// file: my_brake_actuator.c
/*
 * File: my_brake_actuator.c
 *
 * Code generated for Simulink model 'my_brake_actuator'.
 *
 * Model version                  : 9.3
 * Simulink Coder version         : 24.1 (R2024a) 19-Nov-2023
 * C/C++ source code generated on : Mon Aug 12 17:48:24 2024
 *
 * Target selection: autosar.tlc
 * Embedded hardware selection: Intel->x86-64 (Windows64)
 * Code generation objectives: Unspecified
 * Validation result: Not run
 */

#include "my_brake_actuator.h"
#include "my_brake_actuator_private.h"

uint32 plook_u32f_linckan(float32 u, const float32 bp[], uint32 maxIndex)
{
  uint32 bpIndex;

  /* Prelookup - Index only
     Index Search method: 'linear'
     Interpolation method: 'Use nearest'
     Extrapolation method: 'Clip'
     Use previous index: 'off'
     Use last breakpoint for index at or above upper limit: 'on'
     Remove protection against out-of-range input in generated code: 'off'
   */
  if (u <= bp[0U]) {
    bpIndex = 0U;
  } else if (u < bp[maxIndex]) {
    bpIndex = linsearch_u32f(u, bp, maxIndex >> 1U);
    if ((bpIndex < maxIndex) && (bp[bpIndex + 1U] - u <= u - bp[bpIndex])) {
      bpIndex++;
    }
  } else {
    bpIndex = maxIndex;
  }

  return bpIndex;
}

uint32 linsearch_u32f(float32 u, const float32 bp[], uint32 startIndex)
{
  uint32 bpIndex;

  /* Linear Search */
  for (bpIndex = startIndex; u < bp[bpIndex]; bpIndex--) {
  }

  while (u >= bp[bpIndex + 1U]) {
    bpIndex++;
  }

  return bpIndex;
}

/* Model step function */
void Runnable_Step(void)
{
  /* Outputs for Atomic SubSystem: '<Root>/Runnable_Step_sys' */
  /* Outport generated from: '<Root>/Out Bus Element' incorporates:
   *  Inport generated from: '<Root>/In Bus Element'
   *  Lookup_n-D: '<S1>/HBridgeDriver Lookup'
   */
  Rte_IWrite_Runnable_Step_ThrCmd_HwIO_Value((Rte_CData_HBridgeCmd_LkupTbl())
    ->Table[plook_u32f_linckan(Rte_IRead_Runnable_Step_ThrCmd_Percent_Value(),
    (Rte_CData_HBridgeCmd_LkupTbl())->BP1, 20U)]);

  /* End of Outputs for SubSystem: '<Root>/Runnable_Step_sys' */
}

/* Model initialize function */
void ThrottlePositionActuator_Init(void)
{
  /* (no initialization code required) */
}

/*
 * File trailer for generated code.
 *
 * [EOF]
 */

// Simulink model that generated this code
simulink model "my_brake_actuator"  (R2024a)
settings: Solver=FixedStepDiscrete  StartTime=0.0  StopTime=10.0  FixedStep=0.005  RelTol=1e-3
model workspace (MATLAB code in the model file):
  | HBridgeCmd_LkupTbl = Simulink.LookupTable;
  | HBridgeCmd_LkupTbl.Table.DataType = 'int16';
  | HBridgeCmd_LkupTbl.Table.FieldName = 'Table';
  | HBridgeCmd_LkupTbl.Table.Value = int16( ...
  |   [-2048 -1843 -1638 -1434 -1229 -1024 -819 -614 -410 -205 0 205 410 614 ...
  |    819 1024 1229 1434 1638 1843 2048]);
  | HBridgeCmd_LkupTbl.BreakpointsSpecification = 'Explicit values';
  | HBridgeCmd_LkupTbl.SupportTunableSize = false;
  | HBridgeCmd_LkupTbl.Breakpoints.DataType = 'single';
  | HBridgeCmd_LkupTbl.Breakpoints.FieldName = 'BP1';
  | HBridgeCmd_LkupTbl.Breakpoints.Value = ...
  |   [-100 -90 -80 -70 -60 -50 -40 -30 -20 -10 0 10 20 30 40 50 60 70 80 90 ...
  |    100];
  | HBridgeCmd_LkupTbl.Breakpoints.TunableSizeName = 'N1';
  | HBridgeCmd_LkupTbl.StructTypeInfo.Name = 'MyStruct_Actuator';
  | HBridgeCmd_LkupTbl.StructTypeInfo.HeaderFileName = 'Rte_Type.h';
undefined symbols (not defined in the file or in its folder): TPSPercentBkpt, TPSPercentTbl

== system my_brake_actuator ==
  In Bus Element : Inport  PortName=ThrCmd_Percent  Element=Value
  Runnable_Step_sys : Subsystem  TreatAsAtomicUnit=on  SystemSampleTime=0.005
  Out Bus Element : Outport  PortName=ThrCmd_HwIO  Element=Value
  wires:
  In Bus Element/1 -> Runnable_Step_sys/1(ThrCmd_Percent_Value_read)
  Runnable_Step_sys/1(ThrCmd_HwIO_Value_write) -> Out Bus Element/1

== system my_brake_actuator/Runnable_Step_sys ==
  ThrCmd_Percent_Value_read : Inport
  Data Type Conversion : DataTypeConversion  OutDataTypeStr=single  SaturateOnIntegerOverflow=off  RndMeth=Floor
  HBridgeDriver Lookup : Lookup_n-D  NumberOfTableDimensions=1  DataSpecification=Lookup table object  LookupTableObject=HBridgeCmd_LkupTbl  BreakpointsForDimension1=TPSPercentBkpt  BreakpointsForDimension1DataTypeStr=single  IndexSearchMethod=Linear search  Table=TPSPercentTbl  TableDataTypeStr=single  InterpMethod=Nearest  InternalRulePriority=Speed  OutDataTypeStr=Inherit: Inherit from 'Table data'  RndMeth=Simplest
  ThrCmd_HwIO_Value_write : Outport  VectorParamsAs1DForOutWhenUnconnected=off
  wires:
  ThrCmd_Percent_Value_read/1 -> Data Type Conversion/1
  HBridgeDriver Lookup/1 -> ThrCmd_HwIO_Value_write/1
  Data Type Conversion/1 -> HBridgeDriver Lookup/1
